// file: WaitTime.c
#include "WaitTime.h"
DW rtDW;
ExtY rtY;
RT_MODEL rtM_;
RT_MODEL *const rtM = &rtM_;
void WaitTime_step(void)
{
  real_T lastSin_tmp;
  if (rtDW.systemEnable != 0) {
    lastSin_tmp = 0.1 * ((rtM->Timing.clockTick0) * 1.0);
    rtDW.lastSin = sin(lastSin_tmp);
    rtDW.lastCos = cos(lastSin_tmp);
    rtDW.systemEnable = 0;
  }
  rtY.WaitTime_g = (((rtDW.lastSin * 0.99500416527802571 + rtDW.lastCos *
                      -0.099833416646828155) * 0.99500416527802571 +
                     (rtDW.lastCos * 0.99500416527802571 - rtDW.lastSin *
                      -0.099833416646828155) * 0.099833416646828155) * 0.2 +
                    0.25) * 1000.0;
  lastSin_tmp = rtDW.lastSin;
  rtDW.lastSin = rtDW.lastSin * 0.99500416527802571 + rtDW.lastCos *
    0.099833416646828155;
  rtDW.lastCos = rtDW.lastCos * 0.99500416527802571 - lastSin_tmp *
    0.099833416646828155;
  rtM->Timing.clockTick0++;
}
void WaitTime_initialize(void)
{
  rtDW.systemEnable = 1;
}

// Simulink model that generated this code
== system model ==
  WaitTime : Outport  <- 1: Gain#1
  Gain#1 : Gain  Gain=1000  <- 1: Sin#1
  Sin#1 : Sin  Amplitude=0.2  Bias=0.25  Frequency=0.1
